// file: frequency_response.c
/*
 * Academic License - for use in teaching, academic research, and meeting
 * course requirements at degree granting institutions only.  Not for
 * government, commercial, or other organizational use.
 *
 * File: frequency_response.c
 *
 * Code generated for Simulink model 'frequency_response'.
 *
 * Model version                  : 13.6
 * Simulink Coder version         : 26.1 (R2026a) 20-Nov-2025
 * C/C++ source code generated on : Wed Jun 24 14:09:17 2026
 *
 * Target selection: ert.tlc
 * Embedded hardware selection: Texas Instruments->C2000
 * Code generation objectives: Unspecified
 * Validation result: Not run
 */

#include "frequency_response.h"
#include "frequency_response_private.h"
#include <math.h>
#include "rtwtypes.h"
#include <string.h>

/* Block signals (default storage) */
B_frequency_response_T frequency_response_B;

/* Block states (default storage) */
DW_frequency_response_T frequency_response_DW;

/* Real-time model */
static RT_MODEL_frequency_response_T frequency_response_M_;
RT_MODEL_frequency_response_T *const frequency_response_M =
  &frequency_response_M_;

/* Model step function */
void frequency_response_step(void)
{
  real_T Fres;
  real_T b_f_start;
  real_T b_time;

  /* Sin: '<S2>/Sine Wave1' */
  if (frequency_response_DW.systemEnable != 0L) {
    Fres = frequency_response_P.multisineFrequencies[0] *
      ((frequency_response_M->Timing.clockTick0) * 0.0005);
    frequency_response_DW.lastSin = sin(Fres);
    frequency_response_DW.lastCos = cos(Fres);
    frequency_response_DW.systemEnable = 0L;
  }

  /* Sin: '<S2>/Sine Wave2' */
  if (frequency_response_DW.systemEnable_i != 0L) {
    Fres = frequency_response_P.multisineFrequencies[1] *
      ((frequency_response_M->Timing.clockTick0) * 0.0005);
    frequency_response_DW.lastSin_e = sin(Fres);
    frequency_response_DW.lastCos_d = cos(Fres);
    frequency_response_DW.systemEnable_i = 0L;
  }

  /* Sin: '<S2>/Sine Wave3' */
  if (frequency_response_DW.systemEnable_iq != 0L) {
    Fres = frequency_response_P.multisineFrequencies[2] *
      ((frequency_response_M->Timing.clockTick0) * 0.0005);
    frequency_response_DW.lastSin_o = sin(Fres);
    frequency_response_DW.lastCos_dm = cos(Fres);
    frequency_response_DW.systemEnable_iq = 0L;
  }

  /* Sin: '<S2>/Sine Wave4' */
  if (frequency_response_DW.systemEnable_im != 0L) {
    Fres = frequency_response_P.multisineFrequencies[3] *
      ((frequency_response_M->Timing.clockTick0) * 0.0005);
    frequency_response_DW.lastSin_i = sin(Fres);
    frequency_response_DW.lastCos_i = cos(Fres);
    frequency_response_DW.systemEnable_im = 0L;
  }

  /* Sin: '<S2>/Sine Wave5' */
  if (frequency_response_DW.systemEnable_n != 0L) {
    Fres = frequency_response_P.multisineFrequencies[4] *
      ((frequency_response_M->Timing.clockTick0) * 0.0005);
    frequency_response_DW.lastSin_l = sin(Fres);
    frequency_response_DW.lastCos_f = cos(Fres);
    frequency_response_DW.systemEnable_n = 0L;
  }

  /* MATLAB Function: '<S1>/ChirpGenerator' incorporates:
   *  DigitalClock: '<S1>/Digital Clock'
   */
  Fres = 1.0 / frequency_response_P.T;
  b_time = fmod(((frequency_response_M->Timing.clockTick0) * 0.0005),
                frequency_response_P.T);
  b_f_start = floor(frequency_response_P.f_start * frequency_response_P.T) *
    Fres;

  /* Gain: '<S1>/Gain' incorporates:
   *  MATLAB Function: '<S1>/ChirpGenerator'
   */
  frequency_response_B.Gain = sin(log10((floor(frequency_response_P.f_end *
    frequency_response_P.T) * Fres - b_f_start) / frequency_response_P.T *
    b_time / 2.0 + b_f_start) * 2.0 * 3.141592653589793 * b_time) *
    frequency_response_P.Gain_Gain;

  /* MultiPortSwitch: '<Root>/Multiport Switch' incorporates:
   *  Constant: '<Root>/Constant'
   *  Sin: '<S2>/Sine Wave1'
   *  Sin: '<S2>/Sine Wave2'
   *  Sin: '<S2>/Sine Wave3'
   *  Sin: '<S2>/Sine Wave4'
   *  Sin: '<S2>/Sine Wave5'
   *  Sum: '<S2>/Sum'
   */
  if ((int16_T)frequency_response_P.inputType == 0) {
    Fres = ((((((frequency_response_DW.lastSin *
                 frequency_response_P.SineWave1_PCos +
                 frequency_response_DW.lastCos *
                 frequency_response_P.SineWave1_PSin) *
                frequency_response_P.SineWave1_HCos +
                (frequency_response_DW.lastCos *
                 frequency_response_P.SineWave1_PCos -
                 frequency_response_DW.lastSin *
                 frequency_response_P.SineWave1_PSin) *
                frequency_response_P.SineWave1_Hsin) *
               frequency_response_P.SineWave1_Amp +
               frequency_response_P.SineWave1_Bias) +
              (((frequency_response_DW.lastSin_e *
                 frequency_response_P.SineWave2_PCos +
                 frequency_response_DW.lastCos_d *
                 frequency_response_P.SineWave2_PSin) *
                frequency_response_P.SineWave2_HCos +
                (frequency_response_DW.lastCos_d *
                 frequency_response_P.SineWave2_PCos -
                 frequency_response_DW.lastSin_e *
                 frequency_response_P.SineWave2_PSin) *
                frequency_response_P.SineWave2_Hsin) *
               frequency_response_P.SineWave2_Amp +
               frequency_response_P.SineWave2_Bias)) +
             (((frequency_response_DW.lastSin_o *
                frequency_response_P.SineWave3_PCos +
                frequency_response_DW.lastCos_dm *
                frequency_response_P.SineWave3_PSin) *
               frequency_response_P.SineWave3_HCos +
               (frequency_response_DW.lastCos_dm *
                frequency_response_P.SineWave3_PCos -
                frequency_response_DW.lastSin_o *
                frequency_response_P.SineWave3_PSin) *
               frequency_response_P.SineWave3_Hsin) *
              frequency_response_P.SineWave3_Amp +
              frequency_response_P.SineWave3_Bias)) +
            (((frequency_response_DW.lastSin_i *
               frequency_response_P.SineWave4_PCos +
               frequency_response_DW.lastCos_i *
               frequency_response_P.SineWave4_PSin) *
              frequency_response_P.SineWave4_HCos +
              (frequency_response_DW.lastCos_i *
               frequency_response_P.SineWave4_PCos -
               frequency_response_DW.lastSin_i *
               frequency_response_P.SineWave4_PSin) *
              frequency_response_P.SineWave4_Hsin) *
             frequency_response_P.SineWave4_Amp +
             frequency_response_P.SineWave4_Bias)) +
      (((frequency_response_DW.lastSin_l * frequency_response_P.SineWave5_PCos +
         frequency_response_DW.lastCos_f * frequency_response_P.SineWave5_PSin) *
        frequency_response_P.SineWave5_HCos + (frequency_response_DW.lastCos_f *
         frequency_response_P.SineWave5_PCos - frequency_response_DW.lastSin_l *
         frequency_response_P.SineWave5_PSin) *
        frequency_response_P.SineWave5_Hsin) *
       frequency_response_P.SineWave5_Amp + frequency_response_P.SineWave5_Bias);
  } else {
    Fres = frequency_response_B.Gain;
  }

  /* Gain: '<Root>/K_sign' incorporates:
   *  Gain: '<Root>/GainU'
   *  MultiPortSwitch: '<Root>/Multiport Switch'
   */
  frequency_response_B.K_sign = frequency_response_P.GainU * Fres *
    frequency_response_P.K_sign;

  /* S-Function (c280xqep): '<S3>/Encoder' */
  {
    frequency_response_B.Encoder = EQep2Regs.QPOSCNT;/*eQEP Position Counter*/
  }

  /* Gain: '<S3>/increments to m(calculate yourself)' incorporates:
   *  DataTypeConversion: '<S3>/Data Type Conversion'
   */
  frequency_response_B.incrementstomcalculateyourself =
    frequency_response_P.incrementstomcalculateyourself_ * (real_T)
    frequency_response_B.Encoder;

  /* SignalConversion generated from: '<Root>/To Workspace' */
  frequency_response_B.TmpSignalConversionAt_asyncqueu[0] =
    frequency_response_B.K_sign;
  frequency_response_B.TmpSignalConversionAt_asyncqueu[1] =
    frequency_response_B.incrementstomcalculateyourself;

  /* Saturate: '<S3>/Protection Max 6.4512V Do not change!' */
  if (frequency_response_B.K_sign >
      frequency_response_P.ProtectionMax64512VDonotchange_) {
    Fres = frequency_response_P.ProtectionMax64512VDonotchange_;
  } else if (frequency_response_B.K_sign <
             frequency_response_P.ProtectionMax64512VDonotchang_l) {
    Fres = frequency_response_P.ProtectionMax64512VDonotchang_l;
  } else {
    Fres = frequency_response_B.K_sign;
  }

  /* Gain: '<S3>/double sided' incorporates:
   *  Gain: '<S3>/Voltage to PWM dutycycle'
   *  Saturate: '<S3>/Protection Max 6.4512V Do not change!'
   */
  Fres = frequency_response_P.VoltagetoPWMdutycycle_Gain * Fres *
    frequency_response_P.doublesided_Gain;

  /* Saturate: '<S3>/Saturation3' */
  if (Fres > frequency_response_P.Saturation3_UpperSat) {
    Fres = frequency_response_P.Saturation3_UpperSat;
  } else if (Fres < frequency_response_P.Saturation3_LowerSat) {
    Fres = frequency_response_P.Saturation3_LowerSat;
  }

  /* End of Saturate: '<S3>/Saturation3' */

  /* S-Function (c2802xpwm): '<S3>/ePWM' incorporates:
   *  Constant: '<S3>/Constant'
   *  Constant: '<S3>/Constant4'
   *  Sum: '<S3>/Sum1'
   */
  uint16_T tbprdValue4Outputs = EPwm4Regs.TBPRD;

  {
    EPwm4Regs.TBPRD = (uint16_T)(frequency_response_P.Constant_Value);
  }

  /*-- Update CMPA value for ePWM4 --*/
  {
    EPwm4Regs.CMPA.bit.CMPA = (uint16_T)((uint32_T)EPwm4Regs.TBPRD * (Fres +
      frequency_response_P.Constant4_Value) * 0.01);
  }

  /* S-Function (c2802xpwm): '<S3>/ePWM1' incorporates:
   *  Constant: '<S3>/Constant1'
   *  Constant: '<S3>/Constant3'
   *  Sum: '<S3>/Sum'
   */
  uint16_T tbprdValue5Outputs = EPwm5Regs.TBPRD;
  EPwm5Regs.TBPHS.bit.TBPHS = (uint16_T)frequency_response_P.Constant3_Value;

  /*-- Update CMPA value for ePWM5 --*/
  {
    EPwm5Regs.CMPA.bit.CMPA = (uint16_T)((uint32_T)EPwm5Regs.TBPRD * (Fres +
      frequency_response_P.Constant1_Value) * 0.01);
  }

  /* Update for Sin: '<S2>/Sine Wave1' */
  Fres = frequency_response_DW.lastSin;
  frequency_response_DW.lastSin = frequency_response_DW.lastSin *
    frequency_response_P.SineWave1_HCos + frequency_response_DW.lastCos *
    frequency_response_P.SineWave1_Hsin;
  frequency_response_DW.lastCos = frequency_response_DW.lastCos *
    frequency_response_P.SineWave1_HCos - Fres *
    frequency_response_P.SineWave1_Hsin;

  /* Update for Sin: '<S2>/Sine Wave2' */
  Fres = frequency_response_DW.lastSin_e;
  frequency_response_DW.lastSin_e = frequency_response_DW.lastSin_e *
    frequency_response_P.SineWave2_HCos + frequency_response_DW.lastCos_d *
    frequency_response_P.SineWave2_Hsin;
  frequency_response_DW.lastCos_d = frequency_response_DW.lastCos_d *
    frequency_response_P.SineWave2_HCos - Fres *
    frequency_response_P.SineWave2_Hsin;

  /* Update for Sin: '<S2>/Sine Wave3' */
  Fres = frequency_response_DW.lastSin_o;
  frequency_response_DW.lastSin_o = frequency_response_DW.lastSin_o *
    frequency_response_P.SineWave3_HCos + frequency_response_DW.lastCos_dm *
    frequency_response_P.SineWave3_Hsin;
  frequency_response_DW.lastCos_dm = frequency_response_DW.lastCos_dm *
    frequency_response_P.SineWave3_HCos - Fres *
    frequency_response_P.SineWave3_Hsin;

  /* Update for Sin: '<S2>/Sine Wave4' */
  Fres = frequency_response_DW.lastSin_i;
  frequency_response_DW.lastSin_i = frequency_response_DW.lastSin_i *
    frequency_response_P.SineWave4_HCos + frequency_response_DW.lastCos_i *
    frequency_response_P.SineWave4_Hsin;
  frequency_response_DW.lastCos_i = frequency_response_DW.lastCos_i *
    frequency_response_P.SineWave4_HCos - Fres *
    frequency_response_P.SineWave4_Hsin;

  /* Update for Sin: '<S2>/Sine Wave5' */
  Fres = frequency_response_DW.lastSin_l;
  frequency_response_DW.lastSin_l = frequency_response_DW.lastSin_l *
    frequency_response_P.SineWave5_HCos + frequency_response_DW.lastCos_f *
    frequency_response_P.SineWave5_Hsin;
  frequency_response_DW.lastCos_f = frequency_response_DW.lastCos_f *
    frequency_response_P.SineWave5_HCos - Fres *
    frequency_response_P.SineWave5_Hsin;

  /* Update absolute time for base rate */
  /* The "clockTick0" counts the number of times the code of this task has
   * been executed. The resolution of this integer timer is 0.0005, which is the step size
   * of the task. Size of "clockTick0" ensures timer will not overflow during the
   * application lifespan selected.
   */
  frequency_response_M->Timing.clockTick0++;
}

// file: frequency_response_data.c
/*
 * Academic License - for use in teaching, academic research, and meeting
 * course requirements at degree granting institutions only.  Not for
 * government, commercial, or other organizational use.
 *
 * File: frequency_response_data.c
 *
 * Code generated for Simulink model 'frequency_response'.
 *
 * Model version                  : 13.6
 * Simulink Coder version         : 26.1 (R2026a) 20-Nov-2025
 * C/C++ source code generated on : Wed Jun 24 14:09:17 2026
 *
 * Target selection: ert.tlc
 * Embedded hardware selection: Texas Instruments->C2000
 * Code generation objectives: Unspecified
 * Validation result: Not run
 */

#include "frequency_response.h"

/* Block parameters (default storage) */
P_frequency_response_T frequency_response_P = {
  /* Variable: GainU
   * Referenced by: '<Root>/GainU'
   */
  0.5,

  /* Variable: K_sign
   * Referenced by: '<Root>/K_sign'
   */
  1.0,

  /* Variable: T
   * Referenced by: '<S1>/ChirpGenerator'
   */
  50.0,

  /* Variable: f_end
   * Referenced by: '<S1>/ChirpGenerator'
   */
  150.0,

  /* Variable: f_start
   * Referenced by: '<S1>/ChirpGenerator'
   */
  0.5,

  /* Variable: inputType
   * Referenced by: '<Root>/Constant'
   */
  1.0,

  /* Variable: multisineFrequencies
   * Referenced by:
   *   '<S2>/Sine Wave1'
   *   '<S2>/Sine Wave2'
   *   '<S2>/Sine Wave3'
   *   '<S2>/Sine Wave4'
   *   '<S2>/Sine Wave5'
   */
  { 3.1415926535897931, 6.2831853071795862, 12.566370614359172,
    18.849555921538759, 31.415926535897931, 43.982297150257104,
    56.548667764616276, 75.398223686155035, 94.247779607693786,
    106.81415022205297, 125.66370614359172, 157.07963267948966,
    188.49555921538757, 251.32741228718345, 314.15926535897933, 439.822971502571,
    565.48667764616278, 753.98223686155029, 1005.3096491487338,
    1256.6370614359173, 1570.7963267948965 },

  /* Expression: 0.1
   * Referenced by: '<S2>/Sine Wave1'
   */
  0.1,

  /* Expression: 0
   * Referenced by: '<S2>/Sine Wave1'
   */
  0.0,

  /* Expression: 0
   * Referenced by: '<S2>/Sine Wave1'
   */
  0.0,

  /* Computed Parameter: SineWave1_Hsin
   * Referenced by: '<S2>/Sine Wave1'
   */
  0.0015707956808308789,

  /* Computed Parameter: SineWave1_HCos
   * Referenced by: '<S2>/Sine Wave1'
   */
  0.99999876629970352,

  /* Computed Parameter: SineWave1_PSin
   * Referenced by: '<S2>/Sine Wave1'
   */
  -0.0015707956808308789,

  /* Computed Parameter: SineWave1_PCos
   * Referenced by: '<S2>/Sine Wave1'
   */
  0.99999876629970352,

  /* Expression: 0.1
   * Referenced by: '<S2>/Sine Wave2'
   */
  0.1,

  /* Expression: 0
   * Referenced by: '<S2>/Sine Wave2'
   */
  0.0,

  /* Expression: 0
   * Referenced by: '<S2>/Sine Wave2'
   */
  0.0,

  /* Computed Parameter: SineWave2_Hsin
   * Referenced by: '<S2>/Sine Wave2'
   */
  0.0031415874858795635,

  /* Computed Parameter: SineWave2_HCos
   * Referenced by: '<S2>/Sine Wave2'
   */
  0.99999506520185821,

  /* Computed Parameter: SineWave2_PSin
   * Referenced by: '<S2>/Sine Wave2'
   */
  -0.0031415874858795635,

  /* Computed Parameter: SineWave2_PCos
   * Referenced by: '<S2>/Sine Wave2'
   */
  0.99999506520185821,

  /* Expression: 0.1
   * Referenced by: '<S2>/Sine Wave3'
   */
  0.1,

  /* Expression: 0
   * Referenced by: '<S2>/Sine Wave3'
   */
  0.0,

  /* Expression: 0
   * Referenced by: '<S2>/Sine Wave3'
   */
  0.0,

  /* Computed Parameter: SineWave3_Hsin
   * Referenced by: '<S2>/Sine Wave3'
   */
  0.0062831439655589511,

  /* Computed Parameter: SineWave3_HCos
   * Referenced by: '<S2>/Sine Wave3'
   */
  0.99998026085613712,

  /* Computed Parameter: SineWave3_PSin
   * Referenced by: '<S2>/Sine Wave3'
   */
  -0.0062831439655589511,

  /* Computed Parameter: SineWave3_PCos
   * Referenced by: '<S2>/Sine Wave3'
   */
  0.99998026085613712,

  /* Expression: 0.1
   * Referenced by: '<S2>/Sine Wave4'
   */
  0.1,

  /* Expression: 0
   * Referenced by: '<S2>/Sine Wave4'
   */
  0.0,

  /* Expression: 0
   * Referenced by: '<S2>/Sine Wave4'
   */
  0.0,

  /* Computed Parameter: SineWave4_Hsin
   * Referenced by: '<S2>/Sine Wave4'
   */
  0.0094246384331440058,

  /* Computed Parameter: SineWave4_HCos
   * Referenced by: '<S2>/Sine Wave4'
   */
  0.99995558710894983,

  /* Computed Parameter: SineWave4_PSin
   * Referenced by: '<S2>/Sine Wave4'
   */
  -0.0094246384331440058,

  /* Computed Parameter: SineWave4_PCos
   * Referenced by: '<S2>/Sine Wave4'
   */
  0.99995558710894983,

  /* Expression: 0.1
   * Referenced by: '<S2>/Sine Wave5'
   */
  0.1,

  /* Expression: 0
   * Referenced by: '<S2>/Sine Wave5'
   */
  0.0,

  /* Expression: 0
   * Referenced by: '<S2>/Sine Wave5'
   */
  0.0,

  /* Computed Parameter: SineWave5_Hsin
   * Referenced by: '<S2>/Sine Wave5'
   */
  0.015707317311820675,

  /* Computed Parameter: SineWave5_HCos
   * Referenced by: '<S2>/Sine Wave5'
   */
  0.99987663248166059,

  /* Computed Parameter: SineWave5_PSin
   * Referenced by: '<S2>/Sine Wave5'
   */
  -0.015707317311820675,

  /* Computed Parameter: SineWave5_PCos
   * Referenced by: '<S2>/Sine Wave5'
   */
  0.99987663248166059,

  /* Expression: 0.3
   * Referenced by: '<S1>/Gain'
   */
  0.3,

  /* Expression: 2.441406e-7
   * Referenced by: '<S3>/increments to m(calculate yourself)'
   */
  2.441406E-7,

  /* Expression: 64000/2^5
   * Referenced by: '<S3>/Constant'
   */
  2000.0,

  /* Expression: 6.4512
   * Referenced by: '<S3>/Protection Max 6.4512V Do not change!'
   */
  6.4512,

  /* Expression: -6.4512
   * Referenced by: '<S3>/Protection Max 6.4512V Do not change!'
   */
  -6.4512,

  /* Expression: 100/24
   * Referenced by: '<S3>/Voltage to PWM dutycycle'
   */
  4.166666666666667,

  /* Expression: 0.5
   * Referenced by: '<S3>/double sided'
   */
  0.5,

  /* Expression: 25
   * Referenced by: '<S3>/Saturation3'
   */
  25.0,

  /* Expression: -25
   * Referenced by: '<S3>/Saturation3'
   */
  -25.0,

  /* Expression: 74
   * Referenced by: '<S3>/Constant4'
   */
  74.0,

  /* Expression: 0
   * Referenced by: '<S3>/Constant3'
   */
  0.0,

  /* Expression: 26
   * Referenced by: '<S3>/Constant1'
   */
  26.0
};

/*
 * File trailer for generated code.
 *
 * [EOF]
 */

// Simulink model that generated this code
simulink model "frequency_response"  (R2026a)
settings: Solver=FixedStepDiscrete  StopTime=Ttot  FixedStep=ts  EnableMultiTasking=on
values from neighbouring files (symbols this model uses):
  f_end = 250    [frequency_response_initialization.m]
  f_start = 0.5    [frequency_response_initialization.m]
  GainU = 0.2    [frequency_response_initialization.m]
  inputType = 1    [Hm_frd_deliverable_P.mat]    (also in Hm_frd_deliverable_P_smooth.mat; deliverable_p_chirp.mat; frequency_response_identification.m = 0; frequency_response_initialization.m)
  K_sign = 1    [frequency_response_initialization.m]
  multisineFrequencies = 2*pi*multisineFrequencies_Hz    [frequency_response_initialization.m]
  T = 50    [Hm_frd_deliverable_P.mat]    (also in Hm_frd_deliverable_P_smooth.mat; deliverable_p_chirp.mat = 10; frequency_response_initialization.m = 10)
  ts = 0.0005    [Hm_frd_deliverable_P.mat]    (also in Hm_frd_deliverable_P_smooth.mat; deliverable_p_chirp.mat; frequency_response_initialization.m)
undefined symbols (not defined in the file or in its folder): Down, GPTRIP1SEL, GPTRIP2SEL, TZ1, TZ2, Up
libraries: c2802xlib x2, c280xlib x1

== system frequency_response ==
  Angle : Scope
  Chirp : Subsystem
  Constant : Constant  Value=inputType  SampleTime=ts
  GainU : Gain  Gain=GainU
  K_sign : Gain  Gain=K_sign
  Multiport Switch : MultiPortSwitch  DataPortOrder=Zero-based contiguous  Inputs=2  zeroidx=on  SaturateOnIntegerOverflow=off  InputSameDT=off
  Multisine : Subsystem
  Mux : Mux  Inputs=2
  Sensor Displacement : Scope
  To Workspace : ToWorkspace  VariableName=simout  SaveFormat=Structure With Time  SampleTime=ts
  "VCM " : Subsystem
  Voltage : Scope
  displ to angle : Gain  Gain=19.161126
  wires:
  GainU/1 -> K_sign/1
  Mux/1 -> To Workspace/1
  Multisine/1(MultiSine) -> Multiport Switch/2
  "VCM "/1("Position VCM (count) ") -> Mux/2, displ to angle/1, Sensor Displacement/1
  Multiport Switch/1 -> GainU/1
  Chirp/1(Chirp) -> Multiport Switch/3
  Constant/1 -> Multiport Switch/1
  displ to angle/1 -> Angle/1
  K_sign/1 -> "VCM "/1("Voltage (V) "), Voltage/1, Mux/1

== system frequency_response/Chirp ==
  ChirpGenerator : MATLAB Function  TreatAsAtomicUnit=on
  Digital Clock : DigitalClock  SampleTime=ts
  Gain : Gain  Gain=0.3
  Scope : Scope
  Chirp : Outport
  wires:
  Digital Clock/1 -> ChirpGenerator/1(time)
  ChirpGenerator/1(u) -> Gain/1
  Gain/1 -> Scope/1, Chirp/1

== system frequency_response/Multisine ==
  Sine Wave1 : Sin  Amplitude=0.1  Frequency=multisineFrequencies(1)  SampleTime=ts
  Sine Wave2 : Sin  Amplitude=0.1  Frequency=multisineFrequencies(2)  SampleTime=ts
  Sine Wave3 : Sin  Amplitude=0.1  Frequency=multisineFrequencies(3)  SampleTime=ts
  Sine Wave4 : Sin  Amplitude=0.1  Frequency=multisineFrequencies(4)  SampleTime=ts
  Sine Wave5 : Sin  Amplitude=0.1  Frequency=multisineFrequencies(5)  SampleTime=ts
  Sum : Sum  Inputs=+++++
  MultiSine : Outport
  wires:
  Sine Wave5/1 -> Sum/5
  Sine Wave3/1 -> Sum/3
  Sine Wave4/1 -> Sum/4
  Sum/1 -> MultiSine/1
  Sine Wave1/1 -> Sum/1
  Sine Wave2/1 -> Sum/2

== system frequency_response/VCM  ==
  "Voltage (V) " : Inport
  Constant : Constant  Value=64000/2^5
  Constant1 : Constant  Value=26
  Constant3 : Constant  Value=0
  Constant4 : Constant  Value=74
  Data Type Conversion : DataTypeConversion  OutDataTypeStr=double  SaturateOnIntegerOverflow=off  RndMeth=Floor
  Encoder : c280xlib/eQEP  useModule=eQEP2  pcInputmode=Quadrature-count  externalClockrate=2x resolution: Count the rising/falling edge  swapPolarityselection=Clockwise  qdfOutputport=off  qapPolarityselection=off  qbpPolarityselection=off  qipPolarityselection=off  qspPolarityselection=off  igatePolarityselection=off  sampleTime=0.0005  pcOutputport=on  pcMaximumvalue=4294967295  indexInitializationcheck=off  indexInitializationevent=Rising edge  strobeInitializationcheck=off  strobeInitializationevent=Rising edge  softwareInitializationcheck=off  softwareInitializationsource=Set to init value at start up  softwareInitializationmode=on  pcInitialvalue=2147483648  pcResetmode=Reset on the maximum position  ieloutputport=off  indexEventlatch=Rising edge  seloutputport=off  strobeEventlatch=Rising edge  pcefOutputport=off  enableEqepcapture=off  qctmrOutputport=off  qcprdOutputport=off  captureTimerprescaler=128  upEventprescaler=128  overflowErrorflag=off  directionErrorflag=off  captureTimerposition=On position counter read  unitTimerperiod=100000000  captureTimerlatch=off  capturePeriodlatch=off  positionCounterlatch=off  soenPolarityselection=off  spselPolarityselection=Index pin is used for sync output  compareValuesource=Specify via dialog  shadowMode=Load on QPOSCNT=0  compareValue=4294967295  syncOutputwidth=1  polaritySyncoutput=Active high  watchdogEnable=off  watchdogTimer=65535  outport1Datatype=auto  outport2Datatype=int32  outport3Datatype=auto  outport4Datatype=auto  outport5Datatype=auto  outport6Datatype=auto  outport7Datatype=auto  outport8Datatype=auto  outport9Datatype=auto  outport10Datatype=auto  outport11Datatype=auto  outport12Datatype=auto  eqepinterrupt_pce=off  eqepinterrupt_qpe=off  eqepinterrupt_qdc=off  eqepinterrupt_wto=off  eqepinterrupt_pcu=off  eqepinterrupt_pco=off  eqepinterrupt_pcr=off  eqepinterrupt_pcm=off  eqepinterrupt_sel=off  eqepinterrupt_iel=off  eqepinterrupt_uto=off  pheOutputport=off  watchdogOutputport=off  outport13Datatype=auto  outport14Datatype=auto
  Protection Max 6.4512V Do not change! : Saturate  UpperLimit=6.4512  LowerLimit=-6.4512
  Saturation3 : Saturate  UpperLimit=25  LowerLimit=-25
  Sum : Sum  Inputs=|++
  Sum1 : Sum  Inputs=|++
  Voltage to PWM dutycycle : Gain  Gain=100/24
  double sided : Gain  Gain=0.5
  ePWM : c2802xlib/ePWM  PwmType=C2000_Type4  useModule=ePWM4  ePWMxLINKTBPRD=Not Linked  periodUnits=Clock cycles  timerSource=Input port  timerPeriod_clk=64000  timerPeriod_sec=0.0000050  tbshadow=Counter equals to zero  countingMode=Up-Down  phaseActiveEnable=Disable  phaseDirection=Count down after sync  phaseActive=0  synchronizationEnable=off  dcaevt1Sync=off  dcbevt1Sync=off  synchronizationOption=Counter equals to zero (CTR=Zero)  dcbevt1SyncOut=off  dcaevt1SyncOut=off  cmpdSyncOut=off  cmpcSyncOut=off  cmpbSyncOut=off  zeroSyncOut=on  swfSyncOut=off  perSynchronizationOption=Counter equals to period (CTR=PRD)  clockPrescale=1  HSclockPrescale=1  enswap=off  ePWMxAStatus=on  ePWMxAactionLogic1=Set  ePWMxAactionLogic2=Clear  ePWMxAactionLogic3=Clear  ePWMxAactionLogic4=Set  ePWMxAactionLogic5=Do nothing  ePWMxAactionLogic6=Do nothing  ePWMxACSFenable=off  ePWMxACSFvalue=Forcing disable  ePWMxASFreload=Zero  ePWMxBStatus=off  ePWMxBactionLogic1=Set  ePWMxBactionLogic2=Clear  ePWMxBactionLogic3=Do nothing  ePWMxBactionLogic4=Do nothing  ePWMxBactionLogic5=Clear  ePWMxBactionLogic6=Set  ePWMxBCSFenable=off  ePWMxBCSFvalue=Forcing disable  ePWMxBSFreload=Zero  ePWNxBOutWay=off  ePWMxLINKCMPA=Not Linked  CMPAUnits=Percentages  CMPASource=Input port  CMPAValue_per=50  CMPAValue_clk=32000  enCMPAshadow=Counter equals to zero (CTR=Zero)  ePWMxLINKCMPB=Not Linked  CMPBUnits=Clock cycles  CMPBSource=Specify via dialog  CMPBValue_per=50  CMPBValue_clk=32000  enCMPBshadow=Counter equals to zero (CTR=Zero)  ePWMxLINKCMPC=Not Linked  CMPCUnits=Clock cycles  CMPCSource=Specify via dialog  CMPCValue_per=50  CMPCValue_clk=32000  enCMPCshadow=Counter equals to zero (CTR=Zero)  ePWMxLINKCMPD=Not Linked  CMPDUnits=Clock cycles  CMPDSource=Specify via dialog  CMPDValue_per=50  CMPDValue_clk=32000  enCMPDshadow=Counter equals to zero (CTR=Zero)  enableDBePWMxA=off  enableDBePWMxB=off  enhalfcycle=off  DBpolarity=Active high (AH)  DBedgeDelay=Positive  DBSource_ePWMxA=ePWMxA  DBSource_ePWMxB=ePWMxA  DBPeriodUnits=Clock cycles  DBperiodSource=Specify via dialog  REDperiod=0  FEDperiod=0  REDperiod_sec=0  FEDperiod_sec=0  LoadModeDBRED=Immediate without using shadow  LoadModeDBFED=Immediate without using shadow  adcstartModuleA=off  adcrequestEventA=First event  adcstartEventA=Digital Compare Module A Event 1 start of conversion (DCAEVT1.soc)  adcstartEventA_type2=Digital Compare Module A Event 1 start of conversion (DCAEVT1.soc)  adcstartModuleB=off  adcrequestEventB=First event  adcstartEventB=Counter equals to zero (CTR=Zero)  adcstartEventB_type2=Counter equals to zero (CTR=Zero)  intEn=off  intPrd=First event  intSel=Counter equals to zero (CTR=Zero)  intSel_type2=Counter equals to zero (CTR=Zero)  hrpe=off  enHRPWM=off  HRPWM_LoadMode=Counter equals to period (CTR=PRD)  HRPWM_CTLMode=Duty or Period control mode  HRPWM_EDGMode=Both edge  hrpeb=off  enHRPWMB=off  HRPWM_LoadModeB=Counter equals to zero (CTR=ZERO)  HRPWM_CTLModeB=Duty or Period control mode  HRPWM_EDGModeB=Both edge  enHRDBRED=off  enHRDBFED=off  enSFO=on  enautoconv=on  chopperEnable=off  chopperFrequency=1  chopperFirstwidth=1  chopperDuty=12.5%  tripZonesource=Specify via dialog  tzselOSHT1=off  tzselOSHT2=off  tzselOSHT3=off  tzselOSHT4=off  tzselOSHT5=off  tzselOSHT6=off  tzselOSHDCAEV1=off  tzselOSHDCBEV1=off  tzselCBC1=off  tzselCBC2=off  tzselCBC3=off  tzselCBC4=off  tzselCBC5=off  tzselCBC6=off  tzselCBCDCAEV2=off  tzselCBCDCBEV2=off  enTzOstIntr=off  enTzCbcIntr=off  enTzDCAEVT1Intr=off  enTzDCAEVT2Intr=off  enTzDCBEVT1Intr=off  enTzDCBEVT2Intr=off  tzclrCBCLatch=Counter equals to zero (CTR=Zero)  ePWMxAforced=No action  ePWMxBforced=No action  DCAEVT1forced=No action  DCBEVT1forced=No action  DCAEVT2forced=No action  DCBEVT2forced=No action  dcah=Trip Zone 1 input (TZ1)  dcal=Trip Zone 2 input (TZ2)  dcbh=Trip Zone 1 input (TZ1)  dcbl=Trip Zone 2 input (TZ2)  dcah_type2=GPTRIP1SEL/(TZ1)  dcal_type2=GPTRIP2SEL/(TZ2)  dcbh_type2=GPTRIP1SEL/(TZ1)  dcbl_type2=GPTRIP2SEL/(TZ2)  gendcaevt1=Event disabled  gendcaevt2=Event disabled  gendcbevt1=Event disabled  gendcbevt2=Event disabled  dcaevt1src=DCAEVT1 with sync  dcaevt2src=DCAEVT2 with sync  dcbevt1src=DCBEVT1 with sync  dcbevt2src=DCBEVT2 with sync  pulsesel=Counter equals to zero (CTR=Zero)  blankinv=off  blankoffset=0  blankwidth=0  evsrcsel=Filtered version of DCAEVT1 (DCAEVT1FILT)  encape=off
  ePWM1 : c2802xlib/ePWM  PwmType=C2000_Type4  useModule=ePWM5  ePWMxLINKTBPRD=ePWM4  periodUnits=Clock cycles  timerSource=Specify via dialog  timerPeriod_clk=64000  timerPeriod_sec=0.0000025  tbshadow=Counter equals to zero  countingMode=Up-Down  phaseActiveEnable=Set counter to phase value specified via input port  phaseDirection=Count up after sync  phaseActive=0  synchronizationEnable=off  dcaevt1Sync=off  dcbevt1Sync=off  synchronizationOption=Pass through (EPWMxSYNCI or SWFSYNC)  dcbevt1SyncOut=off  dcaevt1SyncOut=off  cmpdSyncOut=off  cmpcSyncOut=off  cmpbSyncOut=off  zeroSyncOut=off  swfSyncOut=on  perSynchronizationOption=Counter equals to period (CTR=PRD)  clockPrescale=1  HSclockPrescale=1  enswap=off  ePWMxAStatus=on  ePWMxAactionLogic1=Clear  ePWMxAactionLogic2=Set  ePWMxAactionLogic3=Set  ePWMxAactionLogic4=Clear  ePWMxAactionLogic5=Do nothing  ePWMxAactionLogic6=Do nothing  ePWMxACSFenable=off  ePWMxACSFvalue=Forcing disable  ePWMxASFreload=Zero  ePWMxBStatus=off  ePWMxBactionLogic1=Set  ePWMxBactionLogic2=Clear  ePWMxBactionLogic3=Do nothing  ePWMxBactionLogic4=Do nothing  ePWMxBactionLogic5=Clear  ePWMxBactionLogic6=Set  ePWMxBCSFenable=off  ePWMxBCSFvalue=Forcing disable  ePWMxBSFreload=Zero  ePWNxBOutWay=off  ePWMxLINKCMPA=Not Linked  CMPAUnits=Percentages  CMPASource=Input port  CMPAValue_per=50  CMPAValue_clk=32000  enCMPAshadow=Counter equals to zero (CTR=Zero)  ePWMxLINKCMPB=Not Linked  CMPBUnits=Clock cycles  CMPBSource=Specify via dialog  CMPBValue_per=50  CMPBValue_clk=32000  enCMPBshadow=Counter equals to zero (CTR=Zero)  ePWMxLINKCMPC=Not Linked  CMPCUnits=Clock cycles  CMPCSource=Specify via dialog  CMPCValue_per=50  CMPCValue_clk=32000  enCMPCshadow=Counter equals to zero (CTR=Zero)  ePWMxLINKCMPD=Not Linked  CMPDUnits=Clock cycles  CMPDSource=Specify via dialog  CMPDValue_per=50  CMPDValue_clk=32000  enCMPDshadow=Counter equals to zero (CTR=Zero)  enableDBePWMxA=off  enableDBePWMxB=off  enhalfcycle=off  DBpolarity=Active high (AH)  DBedgeDelay=Positive  DBSource_ePWMxA=ePWMxA  DBSource_ePWMxB=ePWMxA  DBPeriodUnits=Clock cycles  DBperiodSource=Specify via dialog  REDperiod=0  FEDperiod=0  REDperiod_sec=0  FEDperiod_sec=0  LoadModeDBRED=Immediate without using shadow  LoadModeDBFED=Immediate without using shadow  adcstartModuleA=off  adcrequestEventA=First event  adcstartEventA=Digital Compare Module A Event 1 start of conversion (DCAEVT1.soc)  adcstartEventA_type2=Digital Compare Module A Event 1 start of conversion (DCAEVT1.soc)  adcstartModuleB=off  adcrequestEventB=First event  adcstartEventB=Counter equals to zero (CTR=Zero)  adcstartEventB_type2=Counter equals to zero (CTR=Zero)  intEn=off  intPrd=First event  intSel=Counter equals to zero (CTR=Zero)  intSel_type2=Counter equals to zero (CTR=Zero)  hrpe=off  enHRPWM=off  HRPWM_LoadMode=Counter equals to period (CTR=PRD)  HRPWM_CTLMode=Duty or Period control mode  HRPWM_EDGMode=Both edge  hrpeb=off  enHRPWMB=off  HRPWM_LoadModeB=Counter equals to zero (CTR=ZERO)  HRPWM_CTLModeB=Duty or Period control mode  HRPWM_EDGModeB=Both edge  enHRDBRED=off  enHRDBFED=off  enSFO=on  enautoconv=on  chopperEnable=off  chopperFrequency=1  chopperFirstwidth=1  chopperDuty=12.5%  tripZonesource=Specify via dialog  tzselOSHT1=off  tzselOSHT2=off  tzselOSHT3=off  tzselOSHT4=off  tzselOSHT5=off  tzselOSHT6=off  tzselOSHDCAEV1=off  tzselOSHDCBEV1=off  tzselCBC1=off  tzselCBC2=off  tzselCBC3=off  tzselCBC4=off  tzselCBC5=off  tzselCBC6=off  tzselCBCDCAEV2=off  tzselCBCDCBEV2=off  enTzOstIntr=off  enTzCbcIntr=off  enTzDCAEVT1Intr=off  enTzDCAEVT2Intr=off  enTzDCBEVT1Intr=off  enTzDCBEVT2Intr=off  tzclrCBCLatch=Counter equals to zero (CTR=Zero)  ePWMxAforced=No action  ePWMxBforced=No action  DCAEVT1forced=No action  DCBEVT1forced=No action  DCAEVT2forced=No action  DCBEVT2forced=No action  dcah=Trip Zone 1 input (TZ1)  dcal=Trip Zone 2 input (TZ2)  dcbh=Trip Zone 1 input (TZ1)  dcbl=Trip Zone 2 input (TZ2)  dcah_type2=GPTRIP1SEL/(TZ1)  dcal_type2=GPTRIP2SEL/(TZ2)  dcbh_type2=GPTRIP1SEL/(TZ1)  dcbl_type2=GPTRIP2SEL/(TZ2)  gendcaevt1=Event disabled  gendcaevt2=Event disabled  gendcbevt1=Event disabled  gendcbevt2=Event disabled  dcaevt1src=DCAEVT1 with sync  dcaevt2src=DCAEVT2 with sync  dcbevt1src=DCBEVT1 with sync  dcbevt2src=DCBEVT2 with sync  pulsesel=Counter equals to zero (CTR=Zero)  blankinv=off  blankoffset=0  blankwidth=0  evsrcsel=Filtered version of DCAEVT1 (DCAEVT1FILT)  encape=off
  increments to m(calculate yourself) : Gain  Gain=2.441406e-7
  "Position VCM (count) " : Outport  VectorParamsAs1DForOutWhenUnconnected=off
  wires:
  Data Type Conversion/1 -> increments to m(calculate yourself)/1
  increments to m(calculate yourself)/1 -> "Position VCM (count) "/1
  Encoder/1 -> Data Type Conversion/1
  "Voltage (V) "/1 -> Protection Max 6.4512V Do not change!/1
  Constant1/1 -> Sum/2
  Constant3/1 -> ePWM1/1
  Sum/1 -> ePWM1/2
  Protection Max 6.4512V Do not change!/1 -> Voltage to PWM dutycycle/1
  Constant/1 -> ePWM/1
  Constant4/1 -> Sum1/2
  Saturation3/1 -> Sum/1, Sum1/1
  Sum1/1 -> ePWM/2
  Voltage to PWM dutycycle/1 -> double sided/1
  double sided/1 -> Saturation3/1

== matlab function frequency_response/Chirp/ChirpGenerator ==
function u = ChirpGenerator(time, T, f_start, f_end, ts)
% specify
% ts        [s] sample time
% T         [s] period of sweep
% f_start   [Hz] initial chirp frequency
% f_end     [Hz] final chirp frequency

N = T/ts;                                       % [-] samples per period
Fres = 1/T;                                     % [Hz] frequency resolution / base frequency
time = rem(time,T);                               % [s] wrap time after window;
f_start = floor(f_start*T)*Fres;                % [Hz] round start frequency to multiple of base freuqency (makes input zero at end)
f_end = floor(f_end*T)*Fres;                    % [Hz] round end frequency to multiple of base freuqency (makes input zero at end)
f_act = (f_start + (f_end-f_start)/T*time/2);  % [Hz] frequency of current time sample
u = sin(log10(f_act)*2*pi*time);                      % [iu] input signal (sweep)
